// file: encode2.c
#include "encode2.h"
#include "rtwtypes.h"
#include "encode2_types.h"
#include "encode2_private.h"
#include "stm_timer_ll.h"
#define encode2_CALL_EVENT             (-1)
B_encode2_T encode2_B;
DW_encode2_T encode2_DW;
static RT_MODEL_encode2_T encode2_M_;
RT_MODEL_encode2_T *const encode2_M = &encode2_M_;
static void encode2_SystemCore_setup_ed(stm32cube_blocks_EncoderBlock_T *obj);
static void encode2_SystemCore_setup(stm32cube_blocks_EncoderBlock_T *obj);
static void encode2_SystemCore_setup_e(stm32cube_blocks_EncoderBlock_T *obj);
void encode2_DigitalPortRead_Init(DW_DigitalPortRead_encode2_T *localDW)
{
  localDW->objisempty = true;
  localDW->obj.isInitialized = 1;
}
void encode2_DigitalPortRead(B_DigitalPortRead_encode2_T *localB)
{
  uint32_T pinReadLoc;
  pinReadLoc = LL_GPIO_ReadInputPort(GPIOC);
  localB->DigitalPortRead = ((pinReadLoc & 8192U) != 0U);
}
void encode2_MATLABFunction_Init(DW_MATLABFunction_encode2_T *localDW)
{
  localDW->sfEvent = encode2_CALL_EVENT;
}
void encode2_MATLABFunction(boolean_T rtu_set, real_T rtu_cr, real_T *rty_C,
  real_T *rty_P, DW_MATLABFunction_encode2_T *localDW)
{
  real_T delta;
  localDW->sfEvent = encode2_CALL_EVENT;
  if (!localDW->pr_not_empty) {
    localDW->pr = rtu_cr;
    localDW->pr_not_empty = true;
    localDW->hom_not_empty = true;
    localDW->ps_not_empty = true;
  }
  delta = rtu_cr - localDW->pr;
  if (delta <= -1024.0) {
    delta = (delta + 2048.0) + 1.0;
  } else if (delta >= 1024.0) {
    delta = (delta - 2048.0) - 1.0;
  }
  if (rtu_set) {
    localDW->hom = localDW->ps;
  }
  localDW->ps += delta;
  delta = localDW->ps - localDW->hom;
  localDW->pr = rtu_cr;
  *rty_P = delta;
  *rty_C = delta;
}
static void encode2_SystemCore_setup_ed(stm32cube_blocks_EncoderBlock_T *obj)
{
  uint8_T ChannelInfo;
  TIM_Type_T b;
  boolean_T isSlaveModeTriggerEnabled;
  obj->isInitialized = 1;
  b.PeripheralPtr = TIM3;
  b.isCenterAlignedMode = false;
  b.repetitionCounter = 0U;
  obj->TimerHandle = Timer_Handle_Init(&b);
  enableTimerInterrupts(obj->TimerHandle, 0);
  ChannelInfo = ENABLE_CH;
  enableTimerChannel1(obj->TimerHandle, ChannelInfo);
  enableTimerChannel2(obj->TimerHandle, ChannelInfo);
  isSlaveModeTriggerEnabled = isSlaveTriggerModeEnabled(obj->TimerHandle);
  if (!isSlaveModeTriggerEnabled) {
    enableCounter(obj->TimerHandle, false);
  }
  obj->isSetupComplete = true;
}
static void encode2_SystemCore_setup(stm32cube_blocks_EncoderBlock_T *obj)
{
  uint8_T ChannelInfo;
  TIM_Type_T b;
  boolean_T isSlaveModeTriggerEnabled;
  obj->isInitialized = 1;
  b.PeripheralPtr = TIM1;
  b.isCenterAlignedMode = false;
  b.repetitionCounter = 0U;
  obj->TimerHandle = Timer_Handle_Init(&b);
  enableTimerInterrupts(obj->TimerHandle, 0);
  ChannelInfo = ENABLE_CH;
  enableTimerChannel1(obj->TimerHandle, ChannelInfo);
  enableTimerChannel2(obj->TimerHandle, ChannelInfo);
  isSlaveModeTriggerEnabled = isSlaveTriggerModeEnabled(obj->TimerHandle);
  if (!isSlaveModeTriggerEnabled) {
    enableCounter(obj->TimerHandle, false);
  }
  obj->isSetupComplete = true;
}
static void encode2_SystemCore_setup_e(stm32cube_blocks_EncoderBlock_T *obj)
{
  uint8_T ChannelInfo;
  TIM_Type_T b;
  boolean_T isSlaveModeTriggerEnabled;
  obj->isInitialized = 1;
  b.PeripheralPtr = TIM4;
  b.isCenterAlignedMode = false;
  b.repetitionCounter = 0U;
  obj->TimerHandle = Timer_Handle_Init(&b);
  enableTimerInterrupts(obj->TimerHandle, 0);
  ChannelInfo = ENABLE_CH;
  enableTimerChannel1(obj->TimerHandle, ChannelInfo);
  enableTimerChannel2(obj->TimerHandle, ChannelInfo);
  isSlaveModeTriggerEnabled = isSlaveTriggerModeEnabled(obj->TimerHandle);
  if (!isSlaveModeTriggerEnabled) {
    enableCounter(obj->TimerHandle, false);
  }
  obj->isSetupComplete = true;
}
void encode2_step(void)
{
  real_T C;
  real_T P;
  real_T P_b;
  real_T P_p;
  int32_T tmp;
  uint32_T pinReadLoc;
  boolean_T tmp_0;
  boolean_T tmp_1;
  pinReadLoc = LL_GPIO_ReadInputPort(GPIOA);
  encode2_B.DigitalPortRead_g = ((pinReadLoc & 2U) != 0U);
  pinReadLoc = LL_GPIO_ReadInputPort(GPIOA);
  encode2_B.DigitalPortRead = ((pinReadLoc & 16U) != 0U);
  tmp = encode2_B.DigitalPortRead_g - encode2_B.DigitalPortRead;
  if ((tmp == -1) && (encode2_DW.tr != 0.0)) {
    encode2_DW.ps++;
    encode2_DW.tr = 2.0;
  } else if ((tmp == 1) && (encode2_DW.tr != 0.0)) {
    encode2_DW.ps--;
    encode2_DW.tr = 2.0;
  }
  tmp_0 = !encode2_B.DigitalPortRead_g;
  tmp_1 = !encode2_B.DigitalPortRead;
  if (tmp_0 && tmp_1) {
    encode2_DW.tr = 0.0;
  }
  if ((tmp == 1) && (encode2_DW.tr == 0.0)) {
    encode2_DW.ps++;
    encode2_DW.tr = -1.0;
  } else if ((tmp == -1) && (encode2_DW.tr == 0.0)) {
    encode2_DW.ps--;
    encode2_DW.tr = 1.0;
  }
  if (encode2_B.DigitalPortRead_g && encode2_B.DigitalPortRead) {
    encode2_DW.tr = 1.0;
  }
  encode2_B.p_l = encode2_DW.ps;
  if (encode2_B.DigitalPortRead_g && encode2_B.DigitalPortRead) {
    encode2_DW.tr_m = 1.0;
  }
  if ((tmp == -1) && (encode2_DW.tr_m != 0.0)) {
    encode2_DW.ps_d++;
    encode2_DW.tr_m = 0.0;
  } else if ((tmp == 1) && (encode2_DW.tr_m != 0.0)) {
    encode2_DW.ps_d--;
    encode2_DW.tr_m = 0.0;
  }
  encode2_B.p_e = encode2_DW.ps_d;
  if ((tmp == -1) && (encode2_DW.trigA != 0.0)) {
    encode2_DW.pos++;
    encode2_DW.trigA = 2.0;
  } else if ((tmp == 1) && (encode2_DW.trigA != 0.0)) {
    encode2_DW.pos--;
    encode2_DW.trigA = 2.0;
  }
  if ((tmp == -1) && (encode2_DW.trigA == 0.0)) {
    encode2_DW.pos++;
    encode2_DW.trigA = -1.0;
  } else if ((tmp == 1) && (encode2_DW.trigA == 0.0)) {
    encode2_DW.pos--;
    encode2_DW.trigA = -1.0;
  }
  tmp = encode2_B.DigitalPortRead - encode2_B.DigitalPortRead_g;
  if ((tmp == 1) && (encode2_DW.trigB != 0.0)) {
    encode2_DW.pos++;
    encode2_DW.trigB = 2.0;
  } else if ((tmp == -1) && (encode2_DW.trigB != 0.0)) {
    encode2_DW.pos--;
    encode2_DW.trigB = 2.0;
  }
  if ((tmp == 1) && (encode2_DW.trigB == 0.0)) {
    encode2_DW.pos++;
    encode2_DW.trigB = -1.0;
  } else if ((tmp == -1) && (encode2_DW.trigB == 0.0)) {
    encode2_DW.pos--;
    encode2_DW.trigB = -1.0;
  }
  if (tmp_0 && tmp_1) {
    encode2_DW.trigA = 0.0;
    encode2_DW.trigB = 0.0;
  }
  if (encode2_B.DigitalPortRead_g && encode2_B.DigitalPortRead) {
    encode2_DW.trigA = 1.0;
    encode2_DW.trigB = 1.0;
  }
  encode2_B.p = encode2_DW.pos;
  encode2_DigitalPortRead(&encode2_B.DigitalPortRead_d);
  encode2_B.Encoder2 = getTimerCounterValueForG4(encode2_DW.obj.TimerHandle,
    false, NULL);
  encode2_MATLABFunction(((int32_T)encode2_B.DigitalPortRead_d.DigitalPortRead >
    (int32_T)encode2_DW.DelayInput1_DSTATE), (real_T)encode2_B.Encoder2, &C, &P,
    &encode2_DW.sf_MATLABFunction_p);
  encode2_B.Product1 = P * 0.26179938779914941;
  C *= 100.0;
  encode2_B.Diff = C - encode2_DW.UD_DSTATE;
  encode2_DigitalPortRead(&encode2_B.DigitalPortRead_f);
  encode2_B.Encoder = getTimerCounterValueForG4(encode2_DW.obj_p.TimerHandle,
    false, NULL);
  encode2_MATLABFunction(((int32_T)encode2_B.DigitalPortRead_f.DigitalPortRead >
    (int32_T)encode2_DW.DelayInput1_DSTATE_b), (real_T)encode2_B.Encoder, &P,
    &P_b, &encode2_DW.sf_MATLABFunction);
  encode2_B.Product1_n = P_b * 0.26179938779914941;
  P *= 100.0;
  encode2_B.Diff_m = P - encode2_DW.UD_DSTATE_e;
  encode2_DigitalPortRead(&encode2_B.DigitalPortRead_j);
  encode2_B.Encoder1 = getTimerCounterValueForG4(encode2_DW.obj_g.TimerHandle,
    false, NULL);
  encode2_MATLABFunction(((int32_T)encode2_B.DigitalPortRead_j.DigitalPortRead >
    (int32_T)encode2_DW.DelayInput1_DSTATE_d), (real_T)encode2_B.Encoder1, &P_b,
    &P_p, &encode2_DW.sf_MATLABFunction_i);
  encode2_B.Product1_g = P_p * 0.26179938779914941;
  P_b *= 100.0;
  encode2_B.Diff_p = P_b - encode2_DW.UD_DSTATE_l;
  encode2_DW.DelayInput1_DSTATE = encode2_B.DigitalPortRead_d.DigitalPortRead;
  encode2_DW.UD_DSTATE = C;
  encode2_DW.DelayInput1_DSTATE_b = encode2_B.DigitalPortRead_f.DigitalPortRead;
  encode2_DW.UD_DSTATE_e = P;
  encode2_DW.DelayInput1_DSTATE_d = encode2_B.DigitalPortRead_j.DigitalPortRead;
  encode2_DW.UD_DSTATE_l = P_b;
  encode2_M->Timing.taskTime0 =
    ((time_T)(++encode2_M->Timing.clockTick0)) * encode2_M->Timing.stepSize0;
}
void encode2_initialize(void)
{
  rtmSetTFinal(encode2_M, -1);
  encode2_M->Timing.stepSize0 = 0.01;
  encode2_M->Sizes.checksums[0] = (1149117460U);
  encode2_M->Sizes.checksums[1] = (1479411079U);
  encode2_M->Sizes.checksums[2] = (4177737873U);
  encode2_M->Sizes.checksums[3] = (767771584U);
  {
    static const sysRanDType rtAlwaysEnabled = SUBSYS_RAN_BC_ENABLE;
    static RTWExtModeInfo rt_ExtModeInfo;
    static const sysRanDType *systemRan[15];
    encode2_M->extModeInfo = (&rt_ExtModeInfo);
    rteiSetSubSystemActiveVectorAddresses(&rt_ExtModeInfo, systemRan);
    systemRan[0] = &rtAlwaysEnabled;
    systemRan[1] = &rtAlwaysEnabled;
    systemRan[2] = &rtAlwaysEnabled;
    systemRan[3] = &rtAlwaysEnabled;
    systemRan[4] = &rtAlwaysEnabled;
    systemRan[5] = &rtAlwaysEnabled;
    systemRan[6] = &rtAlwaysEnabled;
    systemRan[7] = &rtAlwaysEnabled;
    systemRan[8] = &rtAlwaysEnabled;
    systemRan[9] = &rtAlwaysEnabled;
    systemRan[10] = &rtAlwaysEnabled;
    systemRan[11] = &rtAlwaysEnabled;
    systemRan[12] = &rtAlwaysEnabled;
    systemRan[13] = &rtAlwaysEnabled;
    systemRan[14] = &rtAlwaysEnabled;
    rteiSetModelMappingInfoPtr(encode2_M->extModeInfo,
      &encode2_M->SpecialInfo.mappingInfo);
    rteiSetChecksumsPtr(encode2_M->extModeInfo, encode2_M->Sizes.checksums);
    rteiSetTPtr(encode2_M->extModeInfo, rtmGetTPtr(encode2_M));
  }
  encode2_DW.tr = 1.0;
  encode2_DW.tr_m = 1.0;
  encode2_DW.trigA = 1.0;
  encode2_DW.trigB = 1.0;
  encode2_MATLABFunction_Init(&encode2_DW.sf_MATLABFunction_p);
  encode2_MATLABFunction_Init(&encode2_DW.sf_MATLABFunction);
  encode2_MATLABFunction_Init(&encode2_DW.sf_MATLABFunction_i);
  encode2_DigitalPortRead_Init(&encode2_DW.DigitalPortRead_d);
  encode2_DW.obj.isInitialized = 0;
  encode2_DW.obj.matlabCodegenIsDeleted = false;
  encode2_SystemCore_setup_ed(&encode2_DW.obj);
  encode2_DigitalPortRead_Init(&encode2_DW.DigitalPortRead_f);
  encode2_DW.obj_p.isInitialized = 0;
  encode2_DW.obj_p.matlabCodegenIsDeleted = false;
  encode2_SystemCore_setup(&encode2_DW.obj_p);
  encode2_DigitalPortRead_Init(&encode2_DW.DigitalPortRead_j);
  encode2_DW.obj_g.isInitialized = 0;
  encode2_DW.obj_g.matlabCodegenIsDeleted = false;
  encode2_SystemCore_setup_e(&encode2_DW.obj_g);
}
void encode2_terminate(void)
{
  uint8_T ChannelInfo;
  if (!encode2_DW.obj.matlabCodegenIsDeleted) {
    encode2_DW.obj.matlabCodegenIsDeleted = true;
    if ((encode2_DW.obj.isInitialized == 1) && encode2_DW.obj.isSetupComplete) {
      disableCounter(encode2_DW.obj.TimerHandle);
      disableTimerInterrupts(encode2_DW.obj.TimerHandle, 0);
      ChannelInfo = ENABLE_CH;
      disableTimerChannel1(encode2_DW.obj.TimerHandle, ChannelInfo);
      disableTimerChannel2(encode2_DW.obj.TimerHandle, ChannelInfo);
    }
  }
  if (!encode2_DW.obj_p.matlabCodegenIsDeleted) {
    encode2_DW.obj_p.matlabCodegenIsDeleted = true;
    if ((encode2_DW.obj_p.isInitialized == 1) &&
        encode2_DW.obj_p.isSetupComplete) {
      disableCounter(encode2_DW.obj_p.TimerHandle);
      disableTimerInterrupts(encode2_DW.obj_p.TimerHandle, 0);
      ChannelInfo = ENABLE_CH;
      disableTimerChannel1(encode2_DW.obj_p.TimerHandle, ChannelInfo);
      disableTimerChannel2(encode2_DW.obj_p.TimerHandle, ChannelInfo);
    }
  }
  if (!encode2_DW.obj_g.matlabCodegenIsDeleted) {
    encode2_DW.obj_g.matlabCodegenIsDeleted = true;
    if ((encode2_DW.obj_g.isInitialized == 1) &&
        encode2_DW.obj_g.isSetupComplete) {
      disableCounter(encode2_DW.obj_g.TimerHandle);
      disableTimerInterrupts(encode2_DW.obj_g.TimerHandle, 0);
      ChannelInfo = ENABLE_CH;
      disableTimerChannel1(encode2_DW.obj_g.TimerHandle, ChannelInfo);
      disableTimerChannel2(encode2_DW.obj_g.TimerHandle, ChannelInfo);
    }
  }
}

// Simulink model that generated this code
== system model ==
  DiscreteDerivative#1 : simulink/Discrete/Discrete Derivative  gainval=1.0  <- 1: MATLABFunction
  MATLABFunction : MATLAB Function  <- 1: DetectRisePositive#1, 2: DataTypeConversion#1
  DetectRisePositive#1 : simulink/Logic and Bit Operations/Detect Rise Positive  <- 1: DigitalPortRead
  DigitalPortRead : stm32f4xxblockslib/Digital Port Read
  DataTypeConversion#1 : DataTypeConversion  <- 1: Encoder
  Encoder : stm32g4xxblockslib/Encoder
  DiscreteDerivative#2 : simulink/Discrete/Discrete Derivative  gainval=1.0  <- 1: MATLABFunction#1
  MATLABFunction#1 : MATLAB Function  <- 1: DetectRisePositive#2, 2: DataTypeConversion#2
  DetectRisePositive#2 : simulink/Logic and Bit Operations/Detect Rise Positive  <- 1: DigitalPortRead#1
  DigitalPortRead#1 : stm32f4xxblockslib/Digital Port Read
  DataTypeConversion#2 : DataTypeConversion  <- 1: Encoder1
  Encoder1 : stm32g4xxblockslib/Encoder
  DiscreteDerivative#3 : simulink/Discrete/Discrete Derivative  gainval=1.0  <- 1: MATLABFunction#2
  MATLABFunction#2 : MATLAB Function  <- 1: DetectRisePositive#3, 2: DataTypeConversion#3
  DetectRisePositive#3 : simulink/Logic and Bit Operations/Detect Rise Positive  <- 1: DigitalPortRead#2
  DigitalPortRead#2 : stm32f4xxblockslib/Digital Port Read
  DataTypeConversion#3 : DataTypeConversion  <- 1: Encoder2
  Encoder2 : stm32g4xxblockslib/Encoder
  MATLABFunction#3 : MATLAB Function  <- 1: DigitalPortRead#3, 2: DigitalPortRead#4
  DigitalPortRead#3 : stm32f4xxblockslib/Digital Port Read
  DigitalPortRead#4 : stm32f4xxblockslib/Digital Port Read
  MATLABFunction#4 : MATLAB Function  <- 1: DigitalPortRead#3, 2: DigitalPortRead#4
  MATLABFunction#5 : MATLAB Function  <- 1: DigitalPortRead#3, 2: DigitalPortRead#4
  Product1 : Product  <- 1: MATLABFunction/2, 2: Constant#1
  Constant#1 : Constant  Value=pi/12
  Product#1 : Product  <- 1: MATLABFunction#1/2, 2: Constant#2
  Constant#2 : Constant  Value=pi/12
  Product#2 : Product  <- 1: MATLABFunction#2/2, 2: Constant#3
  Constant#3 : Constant  Value=pi/12
== matlab function MATLABFunction#3 ==
function p = fcn(a,b)
    persistent pos;
    persistent trig;
    if isempty(trig)
        trig = 1;
        pos = 0;
    end
    if a-b == -1 && trig
        pos = pos + 1;
        trig = 2;
    elseif a-b == 1 && trig
        pos = pos -1;
        trig = 2;
    end

    if a == 0 && b == 0 
        trig = 0;
    end

    if a-b == 1 && trig == 0
        pos = pos + 1;
        trig = -1;
    elseif a-b == -1 && trig == 0
        pos = pos -1;
        trig = 1;
    end

    if a == 1 && b == 1
        trig = 1;
    end
    p = pos;
end

== matlab function MATLABFunction#4 ==
function p = fcn(a,b)
    persistent pos;
    persistent trig;
    if isempty(trig)
        trig = 1;
        pos = 0;
    end
    if a-b == -1 && trig
        pos = pos + 1;
        trig = 0;
    elseif a-b == 1 && trig
        pos = pos -1;
        trig = 0;
    end

    if a == 1 && b == 1
        trig = 1;
    end
    p = pos;
end

== matlab function MATLABFunction#5 ==
function p = fcn(a,b)
    persistent pos;
    persistent trigA;
    persistent trigB;
    if isempty(trigA)
        trigA = 1;
        trigB = 1;
        pos = 0;
    end
    if a-b == -1 && trigA
        pos = pos + 1;
        trigA = 2;
    elseif a-b == 1 && trigA
        pos = pos -1;
        trigA = 2;
    end

    if a-b == -1 && trigA == 0
        pos = pos + 1;
        trigA = -1;
    elseif a-b == 1 && trigA == 0
        pos = pos -1;
        trigA = -1;
    end

    if b-a == 1 && trigB
        pos = pos + 1;
        trigB = 2;
    elseif b-a == -1 && trigB
        pos = pos - 1;
        trigB = 2;
    end

    if b-a == 1 && trigB == 0
        pos = pos + 1;
        trigB = -1;
    elseif b-a == -1 && trigB == 0
        pos = pos - 1;
        trigB = -1;
    end

    if a == 0 && b == 0
        trigA = 0;
        trigB = 0;
    end

    if a == 1 && b == 1
        trigA = 1;
        trigB = 1;
    end
    p = pos;
end

== matlab function MATLAB Function ==
function [C,P] = fcn(set,cr)
    persistent pr;
    persistent hom;
    persistent ps;
    max = 2048;

    if isempty(pr)
        pr = cr;
        hom = 0;
        ps = 0;
    end

    delta = cr - pr;

    if delta <= -1*(max/2)
        delta = delta + max + 1;
    elseif delta >= max/2
        delta = delta -max - 1;
    end

    if set
        hom = ps;
    end
    ps = ps + delta;
    C = ps - hom;
    pr = cr;
    P = C;
end

== matlab function MATLAB Function ==
function [C,P] = fcn(set,cr)
    persistent pr;
    persistent hom;
    persistent ps;
    max = 2048;

    if isempty(pr)
        pr = cr;
        hom = 0;
        ps = 0;
    end

    delta = cr - pr;

    if delta <= -1*(max/2)
        delta = delta + max + 1;
    elseif delta >= max/2
        delta = delta -max - 1;
    end

    if set
        hom = ps;
    end
    ps = ps + delta;
    C = ps - hom;
    pr = cr;
    P = C;
end

== matlab function MATLAB Function ==
function [C,P] = fcn(set,cr)
    persistent pr;
    persistent hom;
    persistent ps;
    max = 2048;

    if isempty(pr)
        pr = cr;
        hom = 0;
        ps = 0;
    end

    delta = cr - pr;

    if delta <= -1*(max/2)
        delta = delta + max + 1;
    elseif delta >= max/2
        delta = delta -max - 1;
    end

    if set
        hom = ps;
    end
    ps = ps + delta;
    C = ps - hom;
    pr = cr;
    P = C;
end
